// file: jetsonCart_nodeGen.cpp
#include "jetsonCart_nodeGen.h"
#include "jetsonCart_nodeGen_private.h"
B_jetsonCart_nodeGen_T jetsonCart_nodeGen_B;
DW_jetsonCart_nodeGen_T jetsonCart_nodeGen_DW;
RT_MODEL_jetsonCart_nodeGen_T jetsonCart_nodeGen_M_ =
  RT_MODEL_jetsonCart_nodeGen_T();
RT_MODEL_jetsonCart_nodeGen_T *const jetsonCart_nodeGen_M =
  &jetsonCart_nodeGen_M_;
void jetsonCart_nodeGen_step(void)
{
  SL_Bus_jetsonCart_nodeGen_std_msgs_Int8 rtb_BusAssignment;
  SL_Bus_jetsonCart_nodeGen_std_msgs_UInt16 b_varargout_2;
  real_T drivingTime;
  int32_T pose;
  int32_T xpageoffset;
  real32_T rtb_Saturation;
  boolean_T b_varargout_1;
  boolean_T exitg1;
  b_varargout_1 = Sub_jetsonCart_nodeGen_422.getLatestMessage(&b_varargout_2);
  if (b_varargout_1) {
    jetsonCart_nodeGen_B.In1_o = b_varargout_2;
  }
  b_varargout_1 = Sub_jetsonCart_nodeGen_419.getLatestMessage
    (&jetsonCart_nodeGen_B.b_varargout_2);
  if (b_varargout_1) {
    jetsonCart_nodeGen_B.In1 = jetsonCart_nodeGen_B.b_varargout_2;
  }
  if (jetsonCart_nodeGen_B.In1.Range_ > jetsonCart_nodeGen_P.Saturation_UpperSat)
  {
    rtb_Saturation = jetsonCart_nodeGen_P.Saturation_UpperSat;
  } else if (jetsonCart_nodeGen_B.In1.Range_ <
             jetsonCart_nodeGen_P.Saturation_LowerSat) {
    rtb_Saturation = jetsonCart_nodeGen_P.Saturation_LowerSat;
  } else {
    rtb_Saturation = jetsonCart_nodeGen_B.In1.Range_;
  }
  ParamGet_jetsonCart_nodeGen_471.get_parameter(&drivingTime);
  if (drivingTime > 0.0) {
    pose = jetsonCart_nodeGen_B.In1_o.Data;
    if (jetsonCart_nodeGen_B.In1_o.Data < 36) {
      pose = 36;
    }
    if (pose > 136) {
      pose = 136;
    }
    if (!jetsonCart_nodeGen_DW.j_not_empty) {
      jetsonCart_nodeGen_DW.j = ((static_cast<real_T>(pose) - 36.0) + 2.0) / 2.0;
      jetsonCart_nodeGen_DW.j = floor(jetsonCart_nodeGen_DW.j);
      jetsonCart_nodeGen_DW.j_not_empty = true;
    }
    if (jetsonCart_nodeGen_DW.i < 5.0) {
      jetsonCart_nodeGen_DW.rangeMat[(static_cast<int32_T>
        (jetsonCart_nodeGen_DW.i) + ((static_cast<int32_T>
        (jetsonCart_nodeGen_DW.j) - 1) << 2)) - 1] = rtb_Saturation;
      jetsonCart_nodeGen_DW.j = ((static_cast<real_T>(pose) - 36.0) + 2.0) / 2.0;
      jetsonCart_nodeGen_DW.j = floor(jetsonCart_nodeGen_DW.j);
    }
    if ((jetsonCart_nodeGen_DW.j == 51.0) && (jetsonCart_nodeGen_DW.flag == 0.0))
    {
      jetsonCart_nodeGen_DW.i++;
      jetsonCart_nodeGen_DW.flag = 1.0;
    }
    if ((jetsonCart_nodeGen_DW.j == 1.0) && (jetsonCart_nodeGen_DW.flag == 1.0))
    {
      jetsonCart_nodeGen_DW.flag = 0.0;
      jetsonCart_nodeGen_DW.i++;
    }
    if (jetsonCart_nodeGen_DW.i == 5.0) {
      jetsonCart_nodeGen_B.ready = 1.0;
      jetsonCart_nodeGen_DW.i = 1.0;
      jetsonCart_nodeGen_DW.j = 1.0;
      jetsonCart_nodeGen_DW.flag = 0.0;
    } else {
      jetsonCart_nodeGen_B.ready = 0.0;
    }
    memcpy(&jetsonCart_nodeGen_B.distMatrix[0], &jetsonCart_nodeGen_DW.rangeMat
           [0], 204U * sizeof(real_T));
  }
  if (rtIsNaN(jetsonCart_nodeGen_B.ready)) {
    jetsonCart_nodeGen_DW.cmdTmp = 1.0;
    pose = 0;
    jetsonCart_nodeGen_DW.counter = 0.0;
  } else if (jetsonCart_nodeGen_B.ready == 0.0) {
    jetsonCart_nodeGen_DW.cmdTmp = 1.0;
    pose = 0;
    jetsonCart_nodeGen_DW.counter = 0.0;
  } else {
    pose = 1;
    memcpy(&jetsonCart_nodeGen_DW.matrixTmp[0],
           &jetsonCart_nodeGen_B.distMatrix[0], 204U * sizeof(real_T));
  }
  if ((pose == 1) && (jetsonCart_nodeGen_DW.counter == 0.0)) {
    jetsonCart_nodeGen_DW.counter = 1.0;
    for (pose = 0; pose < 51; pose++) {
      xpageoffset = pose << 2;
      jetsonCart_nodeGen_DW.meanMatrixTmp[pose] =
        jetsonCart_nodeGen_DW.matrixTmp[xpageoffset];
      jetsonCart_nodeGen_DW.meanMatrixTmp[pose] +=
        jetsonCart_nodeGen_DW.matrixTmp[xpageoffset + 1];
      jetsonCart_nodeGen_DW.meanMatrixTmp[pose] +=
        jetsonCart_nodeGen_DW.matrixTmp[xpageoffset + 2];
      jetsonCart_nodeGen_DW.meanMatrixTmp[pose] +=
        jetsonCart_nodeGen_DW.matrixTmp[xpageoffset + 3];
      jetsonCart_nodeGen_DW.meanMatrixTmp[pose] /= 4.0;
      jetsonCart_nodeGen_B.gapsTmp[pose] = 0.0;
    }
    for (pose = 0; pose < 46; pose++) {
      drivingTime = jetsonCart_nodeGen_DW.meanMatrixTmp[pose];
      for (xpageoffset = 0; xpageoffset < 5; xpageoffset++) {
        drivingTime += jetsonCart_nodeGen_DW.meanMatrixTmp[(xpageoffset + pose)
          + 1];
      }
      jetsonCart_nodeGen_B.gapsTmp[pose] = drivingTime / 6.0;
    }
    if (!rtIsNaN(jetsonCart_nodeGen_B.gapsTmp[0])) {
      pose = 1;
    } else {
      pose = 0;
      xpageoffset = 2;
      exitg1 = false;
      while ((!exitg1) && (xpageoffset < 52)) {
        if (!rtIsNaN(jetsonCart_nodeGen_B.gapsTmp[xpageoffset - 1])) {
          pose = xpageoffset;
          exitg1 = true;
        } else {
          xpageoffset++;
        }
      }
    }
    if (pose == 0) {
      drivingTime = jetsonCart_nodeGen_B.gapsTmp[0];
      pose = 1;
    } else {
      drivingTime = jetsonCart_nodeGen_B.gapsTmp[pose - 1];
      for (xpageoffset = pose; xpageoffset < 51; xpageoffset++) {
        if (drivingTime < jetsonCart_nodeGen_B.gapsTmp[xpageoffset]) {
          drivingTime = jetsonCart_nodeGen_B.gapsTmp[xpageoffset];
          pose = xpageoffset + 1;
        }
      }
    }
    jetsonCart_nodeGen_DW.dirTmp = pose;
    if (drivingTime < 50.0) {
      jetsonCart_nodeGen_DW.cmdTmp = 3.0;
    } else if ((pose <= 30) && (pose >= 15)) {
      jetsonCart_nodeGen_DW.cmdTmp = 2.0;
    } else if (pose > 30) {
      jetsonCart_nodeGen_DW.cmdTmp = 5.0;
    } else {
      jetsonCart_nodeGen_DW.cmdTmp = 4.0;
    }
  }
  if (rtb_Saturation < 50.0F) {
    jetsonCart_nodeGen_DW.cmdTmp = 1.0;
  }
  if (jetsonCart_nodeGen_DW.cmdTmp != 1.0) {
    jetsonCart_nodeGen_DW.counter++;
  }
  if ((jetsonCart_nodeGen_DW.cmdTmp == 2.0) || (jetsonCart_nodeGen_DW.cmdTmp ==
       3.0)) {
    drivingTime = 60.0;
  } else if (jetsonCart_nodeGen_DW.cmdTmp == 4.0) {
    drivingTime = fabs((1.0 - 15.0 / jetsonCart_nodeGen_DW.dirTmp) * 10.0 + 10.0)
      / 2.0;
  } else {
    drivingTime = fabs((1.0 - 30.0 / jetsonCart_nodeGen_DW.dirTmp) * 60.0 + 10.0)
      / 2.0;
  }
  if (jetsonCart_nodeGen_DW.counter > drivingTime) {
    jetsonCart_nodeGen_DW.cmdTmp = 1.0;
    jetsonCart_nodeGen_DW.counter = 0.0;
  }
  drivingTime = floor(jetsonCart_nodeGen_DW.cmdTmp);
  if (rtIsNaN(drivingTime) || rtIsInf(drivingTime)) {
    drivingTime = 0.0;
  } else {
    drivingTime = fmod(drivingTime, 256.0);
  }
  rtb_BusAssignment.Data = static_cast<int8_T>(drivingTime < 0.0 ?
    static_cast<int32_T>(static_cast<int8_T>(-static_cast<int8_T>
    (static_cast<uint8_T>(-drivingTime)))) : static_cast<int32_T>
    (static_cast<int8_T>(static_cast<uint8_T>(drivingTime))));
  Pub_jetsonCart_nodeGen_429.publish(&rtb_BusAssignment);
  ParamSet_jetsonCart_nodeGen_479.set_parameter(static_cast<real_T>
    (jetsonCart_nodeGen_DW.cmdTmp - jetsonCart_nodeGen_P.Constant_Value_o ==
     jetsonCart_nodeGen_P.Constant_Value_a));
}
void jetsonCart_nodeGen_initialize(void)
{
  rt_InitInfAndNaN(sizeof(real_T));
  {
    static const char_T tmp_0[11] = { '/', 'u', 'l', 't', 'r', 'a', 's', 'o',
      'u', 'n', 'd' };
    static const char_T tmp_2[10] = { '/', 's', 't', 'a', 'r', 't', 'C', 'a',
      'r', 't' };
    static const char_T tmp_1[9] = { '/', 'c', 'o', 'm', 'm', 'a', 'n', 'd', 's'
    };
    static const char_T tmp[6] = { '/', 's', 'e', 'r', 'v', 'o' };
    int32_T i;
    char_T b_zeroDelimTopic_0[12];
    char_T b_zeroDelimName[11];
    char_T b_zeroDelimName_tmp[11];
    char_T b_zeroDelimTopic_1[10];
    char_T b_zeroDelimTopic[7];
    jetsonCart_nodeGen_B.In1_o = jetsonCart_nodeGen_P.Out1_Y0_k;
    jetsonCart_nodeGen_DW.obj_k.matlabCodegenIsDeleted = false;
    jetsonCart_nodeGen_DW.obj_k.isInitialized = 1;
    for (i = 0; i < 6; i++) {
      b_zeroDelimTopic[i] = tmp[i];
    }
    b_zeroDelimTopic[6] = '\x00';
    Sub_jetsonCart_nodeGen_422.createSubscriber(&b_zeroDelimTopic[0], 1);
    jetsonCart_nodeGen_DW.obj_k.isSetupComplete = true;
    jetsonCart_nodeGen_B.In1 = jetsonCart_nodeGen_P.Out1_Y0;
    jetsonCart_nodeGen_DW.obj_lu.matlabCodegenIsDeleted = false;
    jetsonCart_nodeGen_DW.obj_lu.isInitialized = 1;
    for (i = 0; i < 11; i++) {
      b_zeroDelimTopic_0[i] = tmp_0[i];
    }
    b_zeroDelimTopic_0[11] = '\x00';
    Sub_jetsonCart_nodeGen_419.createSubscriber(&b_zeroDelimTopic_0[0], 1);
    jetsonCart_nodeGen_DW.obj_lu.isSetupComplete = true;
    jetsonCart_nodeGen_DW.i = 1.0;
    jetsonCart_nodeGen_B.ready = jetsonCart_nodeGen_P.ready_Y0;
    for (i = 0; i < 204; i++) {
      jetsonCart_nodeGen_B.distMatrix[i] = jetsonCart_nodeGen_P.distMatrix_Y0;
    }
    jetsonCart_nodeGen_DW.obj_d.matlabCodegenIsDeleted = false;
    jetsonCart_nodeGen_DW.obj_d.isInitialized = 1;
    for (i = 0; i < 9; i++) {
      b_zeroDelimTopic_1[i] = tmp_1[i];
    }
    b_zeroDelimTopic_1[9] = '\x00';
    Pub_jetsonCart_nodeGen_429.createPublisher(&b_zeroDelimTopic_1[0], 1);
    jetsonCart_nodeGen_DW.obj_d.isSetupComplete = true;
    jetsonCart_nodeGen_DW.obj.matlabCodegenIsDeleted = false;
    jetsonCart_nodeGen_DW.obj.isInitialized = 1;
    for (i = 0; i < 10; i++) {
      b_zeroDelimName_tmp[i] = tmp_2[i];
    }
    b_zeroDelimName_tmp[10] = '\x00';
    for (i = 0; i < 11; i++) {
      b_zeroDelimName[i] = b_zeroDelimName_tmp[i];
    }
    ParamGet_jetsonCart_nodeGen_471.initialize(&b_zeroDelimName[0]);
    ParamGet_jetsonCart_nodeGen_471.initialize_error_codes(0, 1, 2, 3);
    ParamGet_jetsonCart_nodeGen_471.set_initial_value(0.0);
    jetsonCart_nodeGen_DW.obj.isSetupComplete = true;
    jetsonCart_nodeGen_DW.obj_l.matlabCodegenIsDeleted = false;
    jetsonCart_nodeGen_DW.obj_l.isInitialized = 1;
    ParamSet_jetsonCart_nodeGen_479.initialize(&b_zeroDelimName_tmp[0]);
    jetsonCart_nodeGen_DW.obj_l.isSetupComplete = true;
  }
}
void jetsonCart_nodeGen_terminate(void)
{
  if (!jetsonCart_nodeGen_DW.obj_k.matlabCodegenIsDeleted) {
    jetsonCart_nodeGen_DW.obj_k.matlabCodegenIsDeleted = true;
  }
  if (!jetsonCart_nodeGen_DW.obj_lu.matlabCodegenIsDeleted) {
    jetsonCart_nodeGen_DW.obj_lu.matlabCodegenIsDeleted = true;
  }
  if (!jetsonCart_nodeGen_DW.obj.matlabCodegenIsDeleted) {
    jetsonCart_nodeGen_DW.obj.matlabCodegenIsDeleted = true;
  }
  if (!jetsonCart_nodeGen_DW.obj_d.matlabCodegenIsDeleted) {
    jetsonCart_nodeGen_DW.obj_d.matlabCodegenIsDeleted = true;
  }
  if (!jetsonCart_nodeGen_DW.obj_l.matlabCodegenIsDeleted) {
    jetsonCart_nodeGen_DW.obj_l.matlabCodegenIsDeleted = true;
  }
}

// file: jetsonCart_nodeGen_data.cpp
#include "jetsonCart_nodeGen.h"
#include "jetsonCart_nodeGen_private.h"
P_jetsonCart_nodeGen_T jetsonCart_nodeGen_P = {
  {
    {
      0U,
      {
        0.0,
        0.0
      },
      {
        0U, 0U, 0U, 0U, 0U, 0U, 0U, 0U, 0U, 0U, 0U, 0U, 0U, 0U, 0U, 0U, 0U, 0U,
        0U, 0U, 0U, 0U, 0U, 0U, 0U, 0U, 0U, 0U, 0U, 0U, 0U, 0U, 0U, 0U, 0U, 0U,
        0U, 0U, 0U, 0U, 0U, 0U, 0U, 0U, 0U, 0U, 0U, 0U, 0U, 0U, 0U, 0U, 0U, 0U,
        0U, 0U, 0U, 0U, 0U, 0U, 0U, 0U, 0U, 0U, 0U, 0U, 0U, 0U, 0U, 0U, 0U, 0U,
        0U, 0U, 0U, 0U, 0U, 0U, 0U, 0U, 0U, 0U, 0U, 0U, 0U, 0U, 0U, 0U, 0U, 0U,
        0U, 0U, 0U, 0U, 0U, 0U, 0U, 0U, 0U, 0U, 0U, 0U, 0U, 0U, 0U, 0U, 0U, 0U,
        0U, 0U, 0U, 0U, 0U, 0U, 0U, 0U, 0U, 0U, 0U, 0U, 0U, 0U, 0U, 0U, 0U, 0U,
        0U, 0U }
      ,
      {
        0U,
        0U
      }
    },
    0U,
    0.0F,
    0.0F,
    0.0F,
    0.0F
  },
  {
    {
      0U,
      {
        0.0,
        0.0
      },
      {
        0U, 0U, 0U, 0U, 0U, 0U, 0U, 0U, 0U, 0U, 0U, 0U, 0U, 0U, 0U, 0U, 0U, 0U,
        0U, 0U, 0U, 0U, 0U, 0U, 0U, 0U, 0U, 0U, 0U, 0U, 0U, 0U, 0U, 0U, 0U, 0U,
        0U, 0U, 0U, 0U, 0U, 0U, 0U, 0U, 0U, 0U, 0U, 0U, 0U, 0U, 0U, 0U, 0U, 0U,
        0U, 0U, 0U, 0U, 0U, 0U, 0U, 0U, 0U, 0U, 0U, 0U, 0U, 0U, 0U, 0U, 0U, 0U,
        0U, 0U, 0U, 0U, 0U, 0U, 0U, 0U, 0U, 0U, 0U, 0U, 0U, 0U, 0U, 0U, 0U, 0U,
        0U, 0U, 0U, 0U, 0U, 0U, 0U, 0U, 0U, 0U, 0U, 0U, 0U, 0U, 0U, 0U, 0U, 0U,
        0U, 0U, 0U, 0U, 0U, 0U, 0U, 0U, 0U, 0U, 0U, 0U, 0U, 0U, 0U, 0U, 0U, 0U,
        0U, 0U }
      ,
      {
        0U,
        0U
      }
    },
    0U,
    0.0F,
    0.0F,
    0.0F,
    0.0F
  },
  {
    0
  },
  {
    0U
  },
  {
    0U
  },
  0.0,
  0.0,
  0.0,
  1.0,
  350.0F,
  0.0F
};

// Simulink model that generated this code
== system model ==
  Publish#1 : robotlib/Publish  <- 1: BusAssignment
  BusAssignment : BusAssignment  <- 1: BlankMessage#1, 2: DataTypeConversion#1
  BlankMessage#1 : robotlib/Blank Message
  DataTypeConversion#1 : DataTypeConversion  <- 1: Subsystem#1
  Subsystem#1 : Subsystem  <- 1: Subsystem#2, 2: Subsystem#2/2, 3: Saturation
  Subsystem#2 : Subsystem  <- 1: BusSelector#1, 2: Saturation, Enable: GetParameter#1
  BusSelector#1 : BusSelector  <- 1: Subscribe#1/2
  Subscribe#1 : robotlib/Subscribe
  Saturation : Saturate  UpperLimit=350  LowerLimit=0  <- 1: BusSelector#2
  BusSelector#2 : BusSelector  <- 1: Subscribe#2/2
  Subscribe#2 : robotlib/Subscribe
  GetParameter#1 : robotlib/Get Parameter
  SetParameter#1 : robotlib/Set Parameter  <- 1: DataTypeConversion#2
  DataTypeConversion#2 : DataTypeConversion  <- 1: CompareToZero#1
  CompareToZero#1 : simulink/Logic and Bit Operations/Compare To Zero  relop===  <- 1: Sum#1
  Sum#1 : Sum  Inputs=+-  <- 1: Subsystem#1, 2: Constant
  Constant : Constant
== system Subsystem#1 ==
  distMatrix : Inport
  ready : Inport
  Inport#1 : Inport
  Outport#1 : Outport  <- 1: MATLABFunction#1
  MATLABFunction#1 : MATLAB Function  <- 1: distMatrix, 2: ready, 3: Inport#1
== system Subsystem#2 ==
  Inport#2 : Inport
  Range : Inport
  EnablePort#1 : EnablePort
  Outport#2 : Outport  <- 1: MATLABFunction#2
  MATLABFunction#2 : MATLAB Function  <- 1: Range, 2: DataTypeConversion#3
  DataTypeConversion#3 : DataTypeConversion  <- 1: Inport#2
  Outport#3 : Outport  <- 1: MATLABFunction#2/2
== matlab function MATLAB Function ==
function [commands, gapsDir, dirOut, rangeMeanOut, meanMatrixOut]  = fcn(distMatrix, ready, range)%#codegen
persistent doneScanning counter matrixTmp cmdTmp gapsTmp dirTmp rangeTmp meanMatrixTmp

if isempty(matrixTmp)
    matrixTmp = zeros(4,51);
end
if isempty(meanMatrixTmp)
    meanMatrixTmp = zeros(1,51);
end
if isempty(gapsTmp)
    gapsTmp = zeros(1,51);
end
if isempty(rangeTmp)
    rangeTmp = 0;
end
if isempty(dirTmp)
    dirTmp = 0;
end
if isempty(counter)
    counter = 0;
end
if isempty(cmdTmp)
    cmdTmp = 0;
end

if isnan(ready)
    cmdTmp = 1;
    doneScanning = 0;
    counter = 0;
elseif ready == 0
    cmdTmp = 1;
    doneScanning = 0;
    counter = 0;
else
    doneScanning = 1;
    matrixTmp = distMatrix;
end

if doneScanning == 1 && counter == 0
    counter = 1;
    meanMatrix = mean(matrixTmp);
    meanMatrixTmp = meanMatrix;
    gaps = zeros(1,51);
    for i = 1 : length(meanMatrix) - 5
        gaps(i) = mean(meanMatrix(i:i+5));
    end
    gapsTmp = gaps;
    [RangeMean, dir] = max(gaps);
    dirTmp = dir;
    rangeTmp = RangeMean;
    if RangeMean < 50
        cmdTmp = 3;
    else
        if dir <= 30 && dir >= 15
            cmdTmp = 2;
        elseif dir > 30
            cmdTmp = 5;
        else 
            cmdTmp = 4;
        end
    end
end

gapsDir = gapsTmp;
dirOut = dirTmp;
rangeMeanOut = rangeTmp;
meanMatrixOut = meanMatrixTmp;

%servoDir = (dir/51)*100 + 36;

if range < 50 %emergency stop
    cmdTmp = 1;
end

if cmdTmp ~=1
    counter = counter +1;
end

%control
if cmdTmp == 2 || cmdTmp == 3 %driving time for backward or forward drive
    drivingTime = 60;%driving time for backward or forward drive
elseif cmdTmp == 4
    drivingTime = abs((1-15/dirOut)*10 + 10)/2;
else
    drivingTime = abs((1 - 30/dirOut)*60 + 10)/2;
end

if counter > drivingTime
    cmdTmp = 1;
    counter = 0;
end

commands = cmdTmp;

== matlab function MATLAB Function ==
function [distMatrix, ready, col, row] = fcn(range, servoPose)%#codegen
persistent rangeMat i j flag

if isempty(rangeMat)
    rangeMat = zeros(4,51);
end

if isempty(i)
    i = 1;
end

if isempty(flag)
    flag = 0;
end

pose = servoPose;
if pose < 36
    pose = 36;
end
if pose > 136
    pose = 136;
end

if isempty(j)
    j = floor((pose - 36 + 2)/2);
end

if i < 5
    rangeMat(i,j) = range;
%     if flag == 1
%         j = j - 1;
%     else
%         j = j + 1;
%     end
    j = floor((pose - 36 + 2)/2);
end

if  j == 51 && flag == 0
    i = i+1;
    flag = 1;
end
if j == 1 && flag == 1
    flag = 0;
    i = i+1;
end

if  i == 5  
    ready = 1;
    i = 1;
    j = 1;
    flag = 0;
else
    ready = 0;
end

distMatrix = rangeMat;
col = j;
row = i;
